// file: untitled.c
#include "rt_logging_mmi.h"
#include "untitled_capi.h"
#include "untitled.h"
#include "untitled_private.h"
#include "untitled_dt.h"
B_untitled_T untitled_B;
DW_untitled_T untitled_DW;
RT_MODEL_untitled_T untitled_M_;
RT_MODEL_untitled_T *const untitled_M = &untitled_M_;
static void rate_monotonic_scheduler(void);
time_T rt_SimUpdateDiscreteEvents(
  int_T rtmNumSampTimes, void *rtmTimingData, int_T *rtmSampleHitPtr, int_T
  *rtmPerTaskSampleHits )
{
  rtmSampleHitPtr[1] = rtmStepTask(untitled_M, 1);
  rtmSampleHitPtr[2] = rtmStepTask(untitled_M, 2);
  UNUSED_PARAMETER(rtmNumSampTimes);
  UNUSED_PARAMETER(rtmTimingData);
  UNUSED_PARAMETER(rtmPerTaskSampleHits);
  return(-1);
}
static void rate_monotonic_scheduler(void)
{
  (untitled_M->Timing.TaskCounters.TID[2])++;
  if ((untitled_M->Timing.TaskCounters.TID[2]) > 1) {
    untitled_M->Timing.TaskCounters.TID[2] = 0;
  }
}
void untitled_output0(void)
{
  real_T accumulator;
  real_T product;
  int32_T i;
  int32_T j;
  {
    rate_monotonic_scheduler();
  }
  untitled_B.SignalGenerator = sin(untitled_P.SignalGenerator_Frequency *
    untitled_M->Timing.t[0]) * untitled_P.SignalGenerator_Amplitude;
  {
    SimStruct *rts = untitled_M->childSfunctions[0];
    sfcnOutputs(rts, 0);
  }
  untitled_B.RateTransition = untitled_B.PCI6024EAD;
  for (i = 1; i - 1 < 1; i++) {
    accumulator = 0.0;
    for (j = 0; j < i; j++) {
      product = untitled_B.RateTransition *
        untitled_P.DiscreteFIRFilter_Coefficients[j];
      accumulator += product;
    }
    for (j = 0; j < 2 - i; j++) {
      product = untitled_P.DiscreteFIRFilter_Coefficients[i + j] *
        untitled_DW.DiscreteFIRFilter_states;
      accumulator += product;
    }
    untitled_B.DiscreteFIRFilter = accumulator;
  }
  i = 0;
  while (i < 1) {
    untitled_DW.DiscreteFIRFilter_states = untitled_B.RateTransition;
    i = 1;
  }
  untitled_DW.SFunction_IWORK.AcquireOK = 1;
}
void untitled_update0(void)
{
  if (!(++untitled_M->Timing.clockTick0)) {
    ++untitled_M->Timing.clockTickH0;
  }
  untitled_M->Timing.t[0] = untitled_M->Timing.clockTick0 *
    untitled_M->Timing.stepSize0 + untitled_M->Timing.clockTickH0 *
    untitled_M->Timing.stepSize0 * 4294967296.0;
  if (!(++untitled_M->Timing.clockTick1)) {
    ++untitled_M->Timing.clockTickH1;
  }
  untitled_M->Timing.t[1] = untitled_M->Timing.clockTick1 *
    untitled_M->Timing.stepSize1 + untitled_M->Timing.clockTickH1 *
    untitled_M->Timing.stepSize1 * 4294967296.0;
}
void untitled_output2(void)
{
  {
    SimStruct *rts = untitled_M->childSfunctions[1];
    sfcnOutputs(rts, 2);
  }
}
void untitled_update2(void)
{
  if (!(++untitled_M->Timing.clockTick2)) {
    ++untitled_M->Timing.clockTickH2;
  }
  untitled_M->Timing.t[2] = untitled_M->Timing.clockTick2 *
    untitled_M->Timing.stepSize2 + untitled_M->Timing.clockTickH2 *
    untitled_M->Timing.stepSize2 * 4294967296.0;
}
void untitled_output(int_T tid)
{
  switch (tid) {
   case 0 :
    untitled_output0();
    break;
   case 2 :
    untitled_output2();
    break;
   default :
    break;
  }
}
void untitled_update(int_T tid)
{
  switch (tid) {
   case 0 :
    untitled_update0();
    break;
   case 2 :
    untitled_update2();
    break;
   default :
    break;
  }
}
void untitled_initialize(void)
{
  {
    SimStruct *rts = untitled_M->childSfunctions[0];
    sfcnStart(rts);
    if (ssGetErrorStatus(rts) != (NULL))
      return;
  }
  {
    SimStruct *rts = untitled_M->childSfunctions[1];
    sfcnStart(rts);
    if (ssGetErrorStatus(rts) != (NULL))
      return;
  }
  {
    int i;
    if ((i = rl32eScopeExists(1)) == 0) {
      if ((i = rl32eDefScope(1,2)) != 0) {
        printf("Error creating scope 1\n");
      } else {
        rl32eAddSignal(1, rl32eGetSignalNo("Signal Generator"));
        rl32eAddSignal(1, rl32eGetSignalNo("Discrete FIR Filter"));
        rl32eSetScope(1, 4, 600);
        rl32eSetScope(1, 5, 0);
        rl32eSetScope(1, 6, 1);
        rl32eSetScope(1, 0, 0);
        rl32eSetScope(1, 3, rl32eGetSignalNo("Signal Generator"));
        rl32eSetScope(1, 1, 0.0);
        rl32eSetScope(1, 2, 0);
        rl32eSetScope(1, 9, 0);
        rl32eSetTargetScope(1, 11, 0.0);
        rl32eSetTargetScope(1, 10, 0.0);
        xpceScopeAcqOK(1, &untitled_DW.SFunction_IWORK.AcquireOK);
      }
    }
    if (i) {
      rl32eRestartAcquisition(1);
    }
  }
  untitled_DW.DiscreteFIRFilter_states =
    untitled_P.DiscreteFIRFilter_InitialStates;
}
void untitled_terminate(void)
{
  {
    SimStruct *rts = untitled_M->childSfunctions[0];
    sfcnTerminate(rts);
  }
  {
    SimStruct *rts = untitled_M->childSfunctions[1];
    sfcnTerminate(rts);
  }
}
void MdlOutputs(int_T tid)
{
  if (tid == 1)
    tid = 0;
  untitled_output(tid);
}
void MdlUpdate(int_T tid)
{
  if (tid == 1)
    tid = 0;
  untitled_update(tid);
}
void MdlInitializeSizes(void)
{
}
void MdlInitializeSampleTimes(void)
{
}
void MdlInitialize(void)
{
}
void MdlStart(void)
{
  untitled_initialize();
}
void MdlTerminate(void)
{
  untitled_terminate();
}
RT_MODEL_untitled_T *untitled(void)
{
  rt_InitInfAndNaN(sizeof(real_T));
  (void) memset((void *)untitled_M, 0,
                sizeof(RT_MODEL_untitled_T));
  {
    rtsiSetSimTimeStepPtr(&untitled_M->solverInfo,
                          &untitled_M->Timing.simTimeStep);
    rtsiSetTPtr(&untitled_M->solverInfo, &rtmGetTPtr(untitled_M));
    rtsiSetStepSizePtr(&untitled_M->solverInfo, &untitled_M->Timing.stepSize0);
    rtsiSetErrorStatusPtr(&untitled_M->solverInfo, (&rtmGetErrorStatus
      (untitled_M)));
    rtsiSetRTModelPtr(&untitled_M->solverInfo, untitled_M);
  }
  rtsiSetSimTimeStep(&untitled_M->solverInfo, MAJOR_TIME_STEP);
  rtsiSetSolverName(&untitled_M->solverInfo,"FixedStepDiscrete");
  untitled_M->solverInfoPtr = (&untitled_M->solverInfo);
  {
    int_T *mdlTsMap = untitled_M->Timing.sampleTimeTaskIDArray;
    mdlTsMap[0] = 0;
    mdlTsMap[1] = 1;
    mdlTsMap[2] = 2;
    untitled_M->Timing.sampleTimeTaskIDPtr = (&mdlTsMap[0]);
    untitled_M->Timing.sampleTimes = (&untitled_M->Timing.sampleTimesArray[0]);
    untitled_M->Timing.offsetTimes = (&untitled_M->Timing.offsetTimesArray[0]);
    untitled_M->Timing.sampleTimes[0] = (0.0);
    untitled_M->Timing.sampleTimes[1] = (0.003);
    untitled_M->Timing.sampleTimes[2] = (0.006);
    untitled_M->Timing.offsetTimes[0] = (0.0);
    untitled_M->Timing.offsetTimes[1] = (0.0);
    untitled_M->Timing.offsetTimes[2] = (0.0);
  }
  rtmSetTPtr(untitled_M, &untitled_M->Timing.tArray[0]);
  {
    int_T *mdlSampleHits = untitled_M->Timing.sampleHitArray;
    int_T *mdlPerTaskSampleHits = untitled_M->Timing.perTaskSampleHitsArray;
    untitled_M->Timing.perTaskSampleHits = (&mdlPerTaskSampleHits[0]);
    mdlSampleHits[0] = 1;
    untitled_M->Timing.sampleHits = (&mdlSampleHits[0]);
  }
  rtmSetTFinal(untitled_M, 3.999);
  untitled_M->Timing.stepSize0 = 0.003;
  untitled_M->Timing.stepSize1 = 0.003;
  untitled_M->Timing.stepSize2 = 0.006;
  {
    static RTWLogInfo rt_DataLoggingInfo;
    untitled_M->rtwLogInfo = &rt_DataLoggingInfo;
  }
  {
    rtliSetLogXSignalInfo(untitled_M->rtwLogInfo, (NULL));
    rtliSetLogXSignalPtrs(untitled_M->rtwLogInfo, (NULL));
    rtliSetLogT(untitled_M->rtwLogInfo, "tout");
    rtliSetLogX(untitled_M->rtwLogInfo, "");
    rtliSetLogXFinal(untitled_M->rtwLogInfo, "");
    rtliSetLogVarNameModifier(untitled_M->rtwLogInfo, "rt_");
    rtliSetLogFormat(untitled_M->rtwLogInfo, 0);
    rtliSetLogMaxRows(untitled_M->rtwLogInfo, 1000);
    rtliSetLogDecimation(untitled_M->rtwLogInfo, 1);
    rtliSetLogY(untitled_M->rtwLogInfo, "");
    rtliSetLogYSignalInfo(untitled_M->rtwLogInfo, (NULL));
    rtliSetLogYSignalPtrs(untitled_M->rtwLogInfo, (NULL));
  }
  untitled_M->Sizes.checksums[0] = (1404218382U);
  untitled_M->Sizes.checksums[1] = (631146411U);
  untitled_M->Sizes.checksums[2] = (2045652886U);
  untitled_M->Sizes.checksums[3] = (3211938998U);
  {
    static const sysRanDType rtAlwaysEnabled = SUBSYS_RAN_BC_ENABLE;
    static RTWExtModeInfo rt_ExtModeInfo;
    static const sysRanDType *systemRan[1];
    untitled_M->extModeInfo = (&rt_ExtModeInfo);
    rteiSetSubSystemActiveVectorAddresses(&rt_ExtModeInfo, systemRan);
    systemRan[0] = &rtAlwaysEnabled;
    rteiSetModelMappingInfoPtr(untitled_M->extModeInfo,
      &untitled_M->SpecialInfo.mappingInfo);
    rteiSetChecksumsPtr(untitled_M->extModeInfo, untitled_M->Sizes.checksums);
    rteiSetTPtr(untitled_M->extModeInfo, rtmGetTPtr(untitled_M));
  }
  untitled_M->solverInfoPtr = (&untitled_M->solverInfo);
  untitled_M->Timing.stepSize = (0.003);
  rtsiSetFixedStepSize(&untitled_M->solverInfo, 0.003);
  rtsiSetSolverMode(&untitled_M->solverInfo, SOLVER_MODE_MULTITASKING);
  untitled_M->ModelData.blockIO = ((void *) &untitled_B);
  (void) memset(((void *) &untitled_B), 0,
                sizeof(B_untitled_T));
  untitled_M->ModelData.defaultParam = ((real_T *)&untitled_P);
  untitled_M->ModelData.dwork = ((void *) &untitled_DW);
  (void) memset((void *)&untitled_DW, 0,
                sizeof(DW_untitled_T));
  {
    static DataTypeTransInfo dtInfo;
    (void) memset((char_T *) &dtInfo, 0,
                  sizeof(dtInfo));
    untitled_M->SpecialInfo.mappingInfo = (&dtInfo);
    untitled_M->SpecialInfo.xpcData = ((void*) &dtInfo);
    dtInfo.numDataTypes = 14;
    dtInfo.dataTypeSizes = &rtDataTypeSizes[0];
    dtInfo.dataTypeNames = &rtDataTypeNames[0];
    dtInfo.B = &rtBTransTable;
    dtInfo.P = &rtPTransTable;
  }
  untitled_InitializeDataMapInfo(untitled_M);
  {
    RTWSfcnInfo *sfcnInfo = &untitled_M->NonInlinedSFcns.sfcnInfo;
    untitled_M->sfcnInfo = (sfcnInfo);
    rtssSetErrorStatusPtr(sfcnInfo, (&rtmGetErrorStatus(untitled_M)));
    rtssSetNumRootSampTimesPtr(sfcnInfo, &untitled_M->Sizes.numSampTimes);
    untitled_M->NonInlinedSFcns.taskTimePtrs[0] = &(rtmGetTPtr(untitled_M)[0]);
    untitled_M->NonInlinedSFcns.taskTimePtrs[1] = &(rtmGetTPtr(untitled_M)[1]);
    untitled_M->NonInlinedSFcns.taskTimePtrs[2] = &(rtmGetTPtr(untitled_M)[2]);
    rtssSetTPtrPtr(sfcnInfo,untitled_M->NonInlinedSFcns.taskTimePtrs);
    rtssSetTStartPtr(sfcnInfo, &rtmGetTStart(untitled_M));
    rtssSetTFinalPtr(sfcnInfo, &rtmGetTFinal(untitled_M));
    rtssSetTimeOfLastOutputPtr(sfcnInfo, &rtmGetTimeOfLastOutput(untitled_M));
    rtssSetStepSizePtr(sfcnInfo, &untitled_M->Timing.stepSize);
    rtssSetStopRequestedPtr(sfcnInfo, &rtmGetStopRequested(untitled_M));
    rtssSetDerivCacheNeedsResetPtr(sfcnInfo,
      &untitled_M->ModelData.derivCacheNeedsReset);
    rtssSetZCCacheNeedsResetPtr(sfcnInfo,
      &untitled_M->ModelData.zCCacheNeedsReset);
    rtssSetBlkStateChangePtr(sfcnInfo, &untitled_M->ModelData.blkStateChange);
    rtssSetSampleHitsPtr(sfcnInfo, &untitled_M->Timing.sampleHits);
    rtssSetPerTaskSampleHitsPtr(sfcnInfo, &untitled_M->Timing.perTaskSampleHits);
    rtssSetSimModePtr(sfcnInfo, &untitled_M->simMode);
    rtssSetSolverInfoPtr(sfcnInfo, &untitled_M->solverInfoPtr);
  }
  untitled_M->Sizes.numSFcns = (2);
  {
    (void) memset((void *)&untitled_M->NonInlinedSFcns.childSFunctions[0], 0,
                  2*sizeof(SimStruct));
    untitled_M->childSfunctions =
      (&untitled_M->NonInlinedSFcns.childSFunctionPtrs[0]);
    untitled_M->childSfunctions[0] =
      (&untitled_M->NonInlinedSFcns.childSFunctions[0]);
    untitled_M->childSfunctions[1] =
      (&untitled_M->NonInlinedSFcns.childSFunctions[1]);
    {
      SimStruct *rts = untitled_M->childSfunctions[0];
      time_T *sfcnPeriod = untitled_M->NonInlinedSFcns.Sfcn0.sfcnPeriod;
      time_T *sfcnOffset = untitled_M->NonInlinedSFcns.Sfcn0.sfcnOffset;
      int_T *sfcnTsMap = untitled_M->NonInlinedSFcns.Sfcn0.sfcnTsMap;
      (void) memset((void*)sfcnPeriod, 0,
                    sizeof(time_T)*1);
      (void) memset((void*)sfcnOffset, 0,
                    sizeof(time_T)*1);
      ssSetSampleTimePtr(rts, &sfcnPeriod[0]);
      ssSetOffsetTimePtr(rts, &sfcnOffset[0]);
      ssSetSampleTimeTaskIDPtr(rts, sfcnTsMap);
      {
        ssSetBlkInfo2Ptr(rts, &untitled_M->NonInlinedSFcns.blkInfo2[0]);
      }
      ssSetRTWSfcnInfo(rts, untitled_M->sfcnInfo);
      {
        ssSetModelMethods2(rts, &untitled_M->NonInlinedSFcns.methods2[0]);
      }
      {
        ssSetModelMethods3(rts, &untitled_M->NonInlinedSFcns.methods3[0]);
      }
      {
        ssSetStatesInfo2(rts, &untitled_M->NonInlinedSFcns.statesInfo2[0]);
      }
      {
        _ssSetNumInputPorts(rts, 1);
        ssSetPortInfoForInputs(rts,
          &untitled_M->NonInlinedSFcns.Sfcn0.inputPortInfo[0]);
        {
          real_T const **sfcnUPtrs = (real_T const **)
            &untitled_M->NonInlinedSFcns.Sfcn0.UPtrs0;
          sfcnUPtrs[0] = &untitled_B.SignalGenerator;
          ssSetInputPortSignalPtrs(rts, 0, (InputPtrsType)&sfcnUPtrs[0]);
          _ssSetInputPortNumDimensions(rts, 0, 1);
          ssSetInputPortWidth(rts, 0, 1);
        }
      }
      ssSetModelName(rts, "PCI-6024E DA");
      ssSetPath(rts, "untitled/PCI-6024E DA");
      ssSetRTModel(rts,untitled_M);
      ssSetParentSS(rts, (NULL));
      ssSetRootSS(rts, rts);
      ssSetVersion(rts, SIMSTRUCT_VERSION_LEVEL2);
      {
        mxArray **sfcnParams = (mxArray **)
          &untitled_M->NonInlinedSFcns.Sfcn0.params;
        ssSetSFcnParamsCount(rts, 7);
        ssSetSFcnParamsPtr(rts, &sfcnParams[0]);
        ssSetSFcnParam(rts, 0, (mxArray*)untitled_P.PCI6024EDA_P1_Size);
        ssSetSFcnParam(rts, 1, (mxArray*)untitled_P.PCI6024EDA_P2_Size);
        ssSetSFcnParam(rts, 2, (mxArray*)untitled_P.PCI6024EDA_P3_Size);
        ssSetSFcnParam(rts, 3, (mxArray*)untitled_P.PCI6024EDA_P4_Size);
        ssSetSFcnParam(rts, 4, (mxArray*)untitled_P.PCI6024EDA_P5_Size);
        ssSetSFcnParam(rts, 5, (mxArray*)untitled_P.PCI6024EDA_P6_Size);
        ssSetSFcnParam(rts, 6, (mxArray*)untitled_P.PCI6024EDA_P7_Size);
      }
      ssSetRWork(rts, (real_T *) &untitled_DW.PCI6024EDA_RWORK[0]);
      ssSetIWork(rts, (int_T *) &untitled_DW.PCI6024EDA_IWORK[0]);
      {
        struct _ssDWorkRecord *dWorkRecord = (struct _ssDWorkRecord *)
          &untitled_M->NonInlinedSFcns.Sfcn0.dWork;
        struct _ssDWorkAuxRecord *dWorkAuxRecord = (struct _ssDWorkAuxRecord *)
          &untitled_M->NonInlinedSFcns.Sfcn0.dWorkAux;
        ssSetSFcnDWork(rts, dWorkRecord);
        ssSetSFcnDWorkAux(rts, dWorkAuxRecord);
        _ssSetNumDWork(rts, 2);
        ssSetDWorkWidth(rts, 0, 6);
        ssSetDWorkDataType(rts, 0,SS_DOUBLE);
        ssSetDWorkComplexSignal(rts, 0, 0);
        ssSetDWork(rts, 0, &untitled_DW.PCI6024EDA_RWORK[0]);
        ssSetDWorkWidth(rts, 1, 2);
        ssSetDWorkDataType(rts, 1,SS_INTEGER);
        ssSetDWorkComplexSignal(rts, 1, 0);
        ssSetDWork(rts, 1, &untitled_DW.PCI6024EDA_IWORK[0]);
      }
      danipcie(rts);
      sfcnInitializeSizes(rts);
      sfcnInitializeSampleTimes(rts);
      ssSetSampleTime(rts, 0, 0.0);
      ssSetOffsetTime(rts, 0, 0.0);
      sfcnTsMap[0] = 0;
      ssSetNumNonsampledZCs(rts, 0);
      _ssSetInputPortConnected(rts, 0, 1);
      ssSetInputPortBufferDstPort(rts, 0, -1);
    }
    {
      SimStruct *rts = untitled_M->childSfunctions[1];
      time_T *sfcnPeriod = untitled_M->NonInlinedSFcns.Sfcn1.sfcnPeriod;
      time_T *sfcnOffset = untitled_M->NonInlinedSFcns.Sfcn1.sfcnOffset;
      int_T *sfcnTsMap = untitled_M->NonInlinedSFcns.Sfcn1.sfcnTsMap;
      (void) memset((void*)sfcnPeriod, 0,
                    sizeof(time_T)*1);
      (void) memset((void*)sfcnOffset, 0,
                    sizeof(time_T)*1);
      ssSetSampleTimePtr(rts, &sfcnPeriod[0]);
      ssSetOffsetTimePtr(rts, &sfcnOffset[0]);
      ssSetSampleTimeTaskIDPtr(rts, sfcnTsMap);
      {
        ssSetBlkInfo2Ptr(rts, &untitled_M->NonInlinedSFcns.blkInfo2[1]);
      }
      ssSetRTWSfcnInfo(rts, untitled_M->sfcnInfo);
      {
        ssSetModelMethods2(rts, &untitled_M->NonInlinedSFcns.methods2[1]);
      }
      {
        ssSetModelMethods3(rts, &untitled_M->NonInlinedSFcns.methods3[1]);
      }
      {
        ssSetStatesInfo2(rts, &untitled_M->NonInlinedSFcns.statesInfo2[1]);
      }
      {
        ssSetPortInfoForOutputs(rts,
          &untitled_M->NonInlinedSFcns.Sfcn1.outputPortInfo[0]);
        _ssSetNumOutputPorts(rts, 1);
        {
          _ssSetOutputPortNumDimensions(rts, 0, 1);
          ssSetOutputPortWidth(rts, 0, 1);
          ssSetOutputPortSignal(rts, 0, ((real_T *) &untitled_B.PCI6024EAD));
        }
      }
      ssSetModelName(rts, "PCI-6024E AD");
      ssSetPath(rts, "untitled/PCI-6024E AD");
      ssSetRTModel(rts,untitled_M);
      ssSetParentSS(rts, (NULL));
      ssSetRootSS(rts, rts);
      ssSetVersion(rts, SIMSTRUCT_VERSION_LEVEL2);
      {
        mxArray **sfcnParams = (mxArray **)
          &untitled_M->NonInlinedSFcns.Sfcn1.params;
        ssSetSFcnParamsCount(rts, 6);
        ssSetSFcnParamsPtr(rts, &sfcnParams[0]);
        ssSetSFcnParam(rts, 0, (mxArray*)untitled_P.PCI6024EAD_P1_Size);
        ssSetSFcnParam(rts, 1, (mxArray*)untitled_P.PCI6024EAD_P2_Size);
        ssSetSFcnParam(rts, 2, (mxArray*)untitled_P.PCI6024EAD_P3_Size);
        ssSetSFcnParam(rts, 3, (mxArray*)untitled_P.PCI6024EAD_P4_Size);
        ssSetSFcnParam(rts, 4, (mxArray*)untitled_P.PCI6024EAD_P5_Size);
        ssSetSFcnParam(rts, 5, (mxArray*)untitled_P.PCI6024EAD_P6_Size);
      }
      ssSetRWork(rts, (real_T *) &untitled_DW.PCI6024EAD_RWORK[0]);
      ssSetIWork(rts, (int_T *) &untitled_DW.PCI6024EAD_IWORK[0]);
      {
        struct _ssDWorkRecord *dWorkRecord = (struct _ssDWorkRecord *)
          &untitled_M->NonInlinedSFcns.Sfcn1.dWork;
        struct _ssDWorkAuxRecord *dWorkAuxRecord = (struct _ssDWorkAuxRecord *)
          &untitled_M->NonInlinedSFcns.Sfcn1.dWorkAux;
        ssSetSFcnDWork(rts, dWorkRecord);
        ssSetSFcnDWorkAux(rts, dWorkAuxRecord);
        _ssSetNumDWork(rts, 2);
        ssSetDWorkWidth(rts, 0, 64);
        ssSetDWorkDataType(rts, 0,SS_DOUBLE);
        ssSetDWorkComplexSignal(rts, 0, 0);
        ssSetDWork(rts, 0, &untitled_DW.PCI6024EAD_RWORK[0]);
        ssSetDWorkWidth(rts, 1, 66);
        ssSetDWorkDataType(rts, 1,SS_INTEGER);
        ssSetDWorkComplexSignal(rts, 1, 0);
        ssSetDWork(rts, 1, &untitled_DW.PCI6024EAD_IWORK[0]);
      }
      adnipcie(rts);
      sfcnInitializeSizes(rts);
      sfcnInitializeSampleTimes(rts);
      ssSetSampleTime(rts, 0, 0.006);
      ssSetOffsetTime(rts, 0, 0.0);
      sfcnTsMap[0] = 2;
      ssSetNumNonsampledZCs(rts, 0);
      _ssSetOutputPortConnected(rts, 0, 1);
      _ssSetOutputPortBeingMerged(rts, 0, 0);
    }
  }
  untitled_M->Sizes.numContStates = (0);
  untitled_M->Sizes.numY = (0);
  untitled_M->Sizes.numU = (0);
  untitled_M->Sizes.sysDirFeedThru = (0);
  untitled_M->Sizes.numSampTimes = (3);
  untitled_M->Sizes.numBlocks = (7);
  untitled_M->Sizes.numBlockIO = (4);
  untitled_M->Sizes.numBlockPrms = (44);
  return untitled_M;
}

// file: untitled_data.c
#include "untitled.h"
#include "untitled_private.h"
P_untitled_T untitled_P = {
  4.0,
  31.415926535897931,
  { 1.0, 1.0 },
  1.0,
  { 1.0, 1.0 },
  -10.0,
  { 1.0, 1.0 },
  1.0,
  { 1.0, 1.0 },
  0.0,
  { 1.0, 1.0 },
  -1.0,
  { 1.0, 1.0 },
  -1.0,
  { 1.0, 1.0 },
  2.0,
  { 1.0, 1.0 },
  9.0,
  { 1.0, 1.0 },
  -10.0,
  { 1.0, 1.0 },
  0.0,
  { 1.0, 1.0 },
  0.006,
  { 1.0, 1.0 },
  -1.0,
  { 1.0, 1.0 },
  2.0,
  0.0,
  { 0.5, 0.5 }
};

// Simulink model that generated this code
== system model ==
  PCI6024EDA : xpcnilib/D//A/E Series/PCI-6024E DA  <- 1: SignalGenerator
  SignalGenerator : SignalGenerator  Amplitude=4  Frequency=5
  DiscreteFIRFilter : DiscreteFir  <- 1: AsyncRateTransition#1
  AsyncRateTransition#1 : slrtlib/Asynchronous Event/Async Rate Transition  <- 1: PCI6024EAD
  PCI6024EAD : xpcnilib/A//D/E Series/PCI-6024E AD
